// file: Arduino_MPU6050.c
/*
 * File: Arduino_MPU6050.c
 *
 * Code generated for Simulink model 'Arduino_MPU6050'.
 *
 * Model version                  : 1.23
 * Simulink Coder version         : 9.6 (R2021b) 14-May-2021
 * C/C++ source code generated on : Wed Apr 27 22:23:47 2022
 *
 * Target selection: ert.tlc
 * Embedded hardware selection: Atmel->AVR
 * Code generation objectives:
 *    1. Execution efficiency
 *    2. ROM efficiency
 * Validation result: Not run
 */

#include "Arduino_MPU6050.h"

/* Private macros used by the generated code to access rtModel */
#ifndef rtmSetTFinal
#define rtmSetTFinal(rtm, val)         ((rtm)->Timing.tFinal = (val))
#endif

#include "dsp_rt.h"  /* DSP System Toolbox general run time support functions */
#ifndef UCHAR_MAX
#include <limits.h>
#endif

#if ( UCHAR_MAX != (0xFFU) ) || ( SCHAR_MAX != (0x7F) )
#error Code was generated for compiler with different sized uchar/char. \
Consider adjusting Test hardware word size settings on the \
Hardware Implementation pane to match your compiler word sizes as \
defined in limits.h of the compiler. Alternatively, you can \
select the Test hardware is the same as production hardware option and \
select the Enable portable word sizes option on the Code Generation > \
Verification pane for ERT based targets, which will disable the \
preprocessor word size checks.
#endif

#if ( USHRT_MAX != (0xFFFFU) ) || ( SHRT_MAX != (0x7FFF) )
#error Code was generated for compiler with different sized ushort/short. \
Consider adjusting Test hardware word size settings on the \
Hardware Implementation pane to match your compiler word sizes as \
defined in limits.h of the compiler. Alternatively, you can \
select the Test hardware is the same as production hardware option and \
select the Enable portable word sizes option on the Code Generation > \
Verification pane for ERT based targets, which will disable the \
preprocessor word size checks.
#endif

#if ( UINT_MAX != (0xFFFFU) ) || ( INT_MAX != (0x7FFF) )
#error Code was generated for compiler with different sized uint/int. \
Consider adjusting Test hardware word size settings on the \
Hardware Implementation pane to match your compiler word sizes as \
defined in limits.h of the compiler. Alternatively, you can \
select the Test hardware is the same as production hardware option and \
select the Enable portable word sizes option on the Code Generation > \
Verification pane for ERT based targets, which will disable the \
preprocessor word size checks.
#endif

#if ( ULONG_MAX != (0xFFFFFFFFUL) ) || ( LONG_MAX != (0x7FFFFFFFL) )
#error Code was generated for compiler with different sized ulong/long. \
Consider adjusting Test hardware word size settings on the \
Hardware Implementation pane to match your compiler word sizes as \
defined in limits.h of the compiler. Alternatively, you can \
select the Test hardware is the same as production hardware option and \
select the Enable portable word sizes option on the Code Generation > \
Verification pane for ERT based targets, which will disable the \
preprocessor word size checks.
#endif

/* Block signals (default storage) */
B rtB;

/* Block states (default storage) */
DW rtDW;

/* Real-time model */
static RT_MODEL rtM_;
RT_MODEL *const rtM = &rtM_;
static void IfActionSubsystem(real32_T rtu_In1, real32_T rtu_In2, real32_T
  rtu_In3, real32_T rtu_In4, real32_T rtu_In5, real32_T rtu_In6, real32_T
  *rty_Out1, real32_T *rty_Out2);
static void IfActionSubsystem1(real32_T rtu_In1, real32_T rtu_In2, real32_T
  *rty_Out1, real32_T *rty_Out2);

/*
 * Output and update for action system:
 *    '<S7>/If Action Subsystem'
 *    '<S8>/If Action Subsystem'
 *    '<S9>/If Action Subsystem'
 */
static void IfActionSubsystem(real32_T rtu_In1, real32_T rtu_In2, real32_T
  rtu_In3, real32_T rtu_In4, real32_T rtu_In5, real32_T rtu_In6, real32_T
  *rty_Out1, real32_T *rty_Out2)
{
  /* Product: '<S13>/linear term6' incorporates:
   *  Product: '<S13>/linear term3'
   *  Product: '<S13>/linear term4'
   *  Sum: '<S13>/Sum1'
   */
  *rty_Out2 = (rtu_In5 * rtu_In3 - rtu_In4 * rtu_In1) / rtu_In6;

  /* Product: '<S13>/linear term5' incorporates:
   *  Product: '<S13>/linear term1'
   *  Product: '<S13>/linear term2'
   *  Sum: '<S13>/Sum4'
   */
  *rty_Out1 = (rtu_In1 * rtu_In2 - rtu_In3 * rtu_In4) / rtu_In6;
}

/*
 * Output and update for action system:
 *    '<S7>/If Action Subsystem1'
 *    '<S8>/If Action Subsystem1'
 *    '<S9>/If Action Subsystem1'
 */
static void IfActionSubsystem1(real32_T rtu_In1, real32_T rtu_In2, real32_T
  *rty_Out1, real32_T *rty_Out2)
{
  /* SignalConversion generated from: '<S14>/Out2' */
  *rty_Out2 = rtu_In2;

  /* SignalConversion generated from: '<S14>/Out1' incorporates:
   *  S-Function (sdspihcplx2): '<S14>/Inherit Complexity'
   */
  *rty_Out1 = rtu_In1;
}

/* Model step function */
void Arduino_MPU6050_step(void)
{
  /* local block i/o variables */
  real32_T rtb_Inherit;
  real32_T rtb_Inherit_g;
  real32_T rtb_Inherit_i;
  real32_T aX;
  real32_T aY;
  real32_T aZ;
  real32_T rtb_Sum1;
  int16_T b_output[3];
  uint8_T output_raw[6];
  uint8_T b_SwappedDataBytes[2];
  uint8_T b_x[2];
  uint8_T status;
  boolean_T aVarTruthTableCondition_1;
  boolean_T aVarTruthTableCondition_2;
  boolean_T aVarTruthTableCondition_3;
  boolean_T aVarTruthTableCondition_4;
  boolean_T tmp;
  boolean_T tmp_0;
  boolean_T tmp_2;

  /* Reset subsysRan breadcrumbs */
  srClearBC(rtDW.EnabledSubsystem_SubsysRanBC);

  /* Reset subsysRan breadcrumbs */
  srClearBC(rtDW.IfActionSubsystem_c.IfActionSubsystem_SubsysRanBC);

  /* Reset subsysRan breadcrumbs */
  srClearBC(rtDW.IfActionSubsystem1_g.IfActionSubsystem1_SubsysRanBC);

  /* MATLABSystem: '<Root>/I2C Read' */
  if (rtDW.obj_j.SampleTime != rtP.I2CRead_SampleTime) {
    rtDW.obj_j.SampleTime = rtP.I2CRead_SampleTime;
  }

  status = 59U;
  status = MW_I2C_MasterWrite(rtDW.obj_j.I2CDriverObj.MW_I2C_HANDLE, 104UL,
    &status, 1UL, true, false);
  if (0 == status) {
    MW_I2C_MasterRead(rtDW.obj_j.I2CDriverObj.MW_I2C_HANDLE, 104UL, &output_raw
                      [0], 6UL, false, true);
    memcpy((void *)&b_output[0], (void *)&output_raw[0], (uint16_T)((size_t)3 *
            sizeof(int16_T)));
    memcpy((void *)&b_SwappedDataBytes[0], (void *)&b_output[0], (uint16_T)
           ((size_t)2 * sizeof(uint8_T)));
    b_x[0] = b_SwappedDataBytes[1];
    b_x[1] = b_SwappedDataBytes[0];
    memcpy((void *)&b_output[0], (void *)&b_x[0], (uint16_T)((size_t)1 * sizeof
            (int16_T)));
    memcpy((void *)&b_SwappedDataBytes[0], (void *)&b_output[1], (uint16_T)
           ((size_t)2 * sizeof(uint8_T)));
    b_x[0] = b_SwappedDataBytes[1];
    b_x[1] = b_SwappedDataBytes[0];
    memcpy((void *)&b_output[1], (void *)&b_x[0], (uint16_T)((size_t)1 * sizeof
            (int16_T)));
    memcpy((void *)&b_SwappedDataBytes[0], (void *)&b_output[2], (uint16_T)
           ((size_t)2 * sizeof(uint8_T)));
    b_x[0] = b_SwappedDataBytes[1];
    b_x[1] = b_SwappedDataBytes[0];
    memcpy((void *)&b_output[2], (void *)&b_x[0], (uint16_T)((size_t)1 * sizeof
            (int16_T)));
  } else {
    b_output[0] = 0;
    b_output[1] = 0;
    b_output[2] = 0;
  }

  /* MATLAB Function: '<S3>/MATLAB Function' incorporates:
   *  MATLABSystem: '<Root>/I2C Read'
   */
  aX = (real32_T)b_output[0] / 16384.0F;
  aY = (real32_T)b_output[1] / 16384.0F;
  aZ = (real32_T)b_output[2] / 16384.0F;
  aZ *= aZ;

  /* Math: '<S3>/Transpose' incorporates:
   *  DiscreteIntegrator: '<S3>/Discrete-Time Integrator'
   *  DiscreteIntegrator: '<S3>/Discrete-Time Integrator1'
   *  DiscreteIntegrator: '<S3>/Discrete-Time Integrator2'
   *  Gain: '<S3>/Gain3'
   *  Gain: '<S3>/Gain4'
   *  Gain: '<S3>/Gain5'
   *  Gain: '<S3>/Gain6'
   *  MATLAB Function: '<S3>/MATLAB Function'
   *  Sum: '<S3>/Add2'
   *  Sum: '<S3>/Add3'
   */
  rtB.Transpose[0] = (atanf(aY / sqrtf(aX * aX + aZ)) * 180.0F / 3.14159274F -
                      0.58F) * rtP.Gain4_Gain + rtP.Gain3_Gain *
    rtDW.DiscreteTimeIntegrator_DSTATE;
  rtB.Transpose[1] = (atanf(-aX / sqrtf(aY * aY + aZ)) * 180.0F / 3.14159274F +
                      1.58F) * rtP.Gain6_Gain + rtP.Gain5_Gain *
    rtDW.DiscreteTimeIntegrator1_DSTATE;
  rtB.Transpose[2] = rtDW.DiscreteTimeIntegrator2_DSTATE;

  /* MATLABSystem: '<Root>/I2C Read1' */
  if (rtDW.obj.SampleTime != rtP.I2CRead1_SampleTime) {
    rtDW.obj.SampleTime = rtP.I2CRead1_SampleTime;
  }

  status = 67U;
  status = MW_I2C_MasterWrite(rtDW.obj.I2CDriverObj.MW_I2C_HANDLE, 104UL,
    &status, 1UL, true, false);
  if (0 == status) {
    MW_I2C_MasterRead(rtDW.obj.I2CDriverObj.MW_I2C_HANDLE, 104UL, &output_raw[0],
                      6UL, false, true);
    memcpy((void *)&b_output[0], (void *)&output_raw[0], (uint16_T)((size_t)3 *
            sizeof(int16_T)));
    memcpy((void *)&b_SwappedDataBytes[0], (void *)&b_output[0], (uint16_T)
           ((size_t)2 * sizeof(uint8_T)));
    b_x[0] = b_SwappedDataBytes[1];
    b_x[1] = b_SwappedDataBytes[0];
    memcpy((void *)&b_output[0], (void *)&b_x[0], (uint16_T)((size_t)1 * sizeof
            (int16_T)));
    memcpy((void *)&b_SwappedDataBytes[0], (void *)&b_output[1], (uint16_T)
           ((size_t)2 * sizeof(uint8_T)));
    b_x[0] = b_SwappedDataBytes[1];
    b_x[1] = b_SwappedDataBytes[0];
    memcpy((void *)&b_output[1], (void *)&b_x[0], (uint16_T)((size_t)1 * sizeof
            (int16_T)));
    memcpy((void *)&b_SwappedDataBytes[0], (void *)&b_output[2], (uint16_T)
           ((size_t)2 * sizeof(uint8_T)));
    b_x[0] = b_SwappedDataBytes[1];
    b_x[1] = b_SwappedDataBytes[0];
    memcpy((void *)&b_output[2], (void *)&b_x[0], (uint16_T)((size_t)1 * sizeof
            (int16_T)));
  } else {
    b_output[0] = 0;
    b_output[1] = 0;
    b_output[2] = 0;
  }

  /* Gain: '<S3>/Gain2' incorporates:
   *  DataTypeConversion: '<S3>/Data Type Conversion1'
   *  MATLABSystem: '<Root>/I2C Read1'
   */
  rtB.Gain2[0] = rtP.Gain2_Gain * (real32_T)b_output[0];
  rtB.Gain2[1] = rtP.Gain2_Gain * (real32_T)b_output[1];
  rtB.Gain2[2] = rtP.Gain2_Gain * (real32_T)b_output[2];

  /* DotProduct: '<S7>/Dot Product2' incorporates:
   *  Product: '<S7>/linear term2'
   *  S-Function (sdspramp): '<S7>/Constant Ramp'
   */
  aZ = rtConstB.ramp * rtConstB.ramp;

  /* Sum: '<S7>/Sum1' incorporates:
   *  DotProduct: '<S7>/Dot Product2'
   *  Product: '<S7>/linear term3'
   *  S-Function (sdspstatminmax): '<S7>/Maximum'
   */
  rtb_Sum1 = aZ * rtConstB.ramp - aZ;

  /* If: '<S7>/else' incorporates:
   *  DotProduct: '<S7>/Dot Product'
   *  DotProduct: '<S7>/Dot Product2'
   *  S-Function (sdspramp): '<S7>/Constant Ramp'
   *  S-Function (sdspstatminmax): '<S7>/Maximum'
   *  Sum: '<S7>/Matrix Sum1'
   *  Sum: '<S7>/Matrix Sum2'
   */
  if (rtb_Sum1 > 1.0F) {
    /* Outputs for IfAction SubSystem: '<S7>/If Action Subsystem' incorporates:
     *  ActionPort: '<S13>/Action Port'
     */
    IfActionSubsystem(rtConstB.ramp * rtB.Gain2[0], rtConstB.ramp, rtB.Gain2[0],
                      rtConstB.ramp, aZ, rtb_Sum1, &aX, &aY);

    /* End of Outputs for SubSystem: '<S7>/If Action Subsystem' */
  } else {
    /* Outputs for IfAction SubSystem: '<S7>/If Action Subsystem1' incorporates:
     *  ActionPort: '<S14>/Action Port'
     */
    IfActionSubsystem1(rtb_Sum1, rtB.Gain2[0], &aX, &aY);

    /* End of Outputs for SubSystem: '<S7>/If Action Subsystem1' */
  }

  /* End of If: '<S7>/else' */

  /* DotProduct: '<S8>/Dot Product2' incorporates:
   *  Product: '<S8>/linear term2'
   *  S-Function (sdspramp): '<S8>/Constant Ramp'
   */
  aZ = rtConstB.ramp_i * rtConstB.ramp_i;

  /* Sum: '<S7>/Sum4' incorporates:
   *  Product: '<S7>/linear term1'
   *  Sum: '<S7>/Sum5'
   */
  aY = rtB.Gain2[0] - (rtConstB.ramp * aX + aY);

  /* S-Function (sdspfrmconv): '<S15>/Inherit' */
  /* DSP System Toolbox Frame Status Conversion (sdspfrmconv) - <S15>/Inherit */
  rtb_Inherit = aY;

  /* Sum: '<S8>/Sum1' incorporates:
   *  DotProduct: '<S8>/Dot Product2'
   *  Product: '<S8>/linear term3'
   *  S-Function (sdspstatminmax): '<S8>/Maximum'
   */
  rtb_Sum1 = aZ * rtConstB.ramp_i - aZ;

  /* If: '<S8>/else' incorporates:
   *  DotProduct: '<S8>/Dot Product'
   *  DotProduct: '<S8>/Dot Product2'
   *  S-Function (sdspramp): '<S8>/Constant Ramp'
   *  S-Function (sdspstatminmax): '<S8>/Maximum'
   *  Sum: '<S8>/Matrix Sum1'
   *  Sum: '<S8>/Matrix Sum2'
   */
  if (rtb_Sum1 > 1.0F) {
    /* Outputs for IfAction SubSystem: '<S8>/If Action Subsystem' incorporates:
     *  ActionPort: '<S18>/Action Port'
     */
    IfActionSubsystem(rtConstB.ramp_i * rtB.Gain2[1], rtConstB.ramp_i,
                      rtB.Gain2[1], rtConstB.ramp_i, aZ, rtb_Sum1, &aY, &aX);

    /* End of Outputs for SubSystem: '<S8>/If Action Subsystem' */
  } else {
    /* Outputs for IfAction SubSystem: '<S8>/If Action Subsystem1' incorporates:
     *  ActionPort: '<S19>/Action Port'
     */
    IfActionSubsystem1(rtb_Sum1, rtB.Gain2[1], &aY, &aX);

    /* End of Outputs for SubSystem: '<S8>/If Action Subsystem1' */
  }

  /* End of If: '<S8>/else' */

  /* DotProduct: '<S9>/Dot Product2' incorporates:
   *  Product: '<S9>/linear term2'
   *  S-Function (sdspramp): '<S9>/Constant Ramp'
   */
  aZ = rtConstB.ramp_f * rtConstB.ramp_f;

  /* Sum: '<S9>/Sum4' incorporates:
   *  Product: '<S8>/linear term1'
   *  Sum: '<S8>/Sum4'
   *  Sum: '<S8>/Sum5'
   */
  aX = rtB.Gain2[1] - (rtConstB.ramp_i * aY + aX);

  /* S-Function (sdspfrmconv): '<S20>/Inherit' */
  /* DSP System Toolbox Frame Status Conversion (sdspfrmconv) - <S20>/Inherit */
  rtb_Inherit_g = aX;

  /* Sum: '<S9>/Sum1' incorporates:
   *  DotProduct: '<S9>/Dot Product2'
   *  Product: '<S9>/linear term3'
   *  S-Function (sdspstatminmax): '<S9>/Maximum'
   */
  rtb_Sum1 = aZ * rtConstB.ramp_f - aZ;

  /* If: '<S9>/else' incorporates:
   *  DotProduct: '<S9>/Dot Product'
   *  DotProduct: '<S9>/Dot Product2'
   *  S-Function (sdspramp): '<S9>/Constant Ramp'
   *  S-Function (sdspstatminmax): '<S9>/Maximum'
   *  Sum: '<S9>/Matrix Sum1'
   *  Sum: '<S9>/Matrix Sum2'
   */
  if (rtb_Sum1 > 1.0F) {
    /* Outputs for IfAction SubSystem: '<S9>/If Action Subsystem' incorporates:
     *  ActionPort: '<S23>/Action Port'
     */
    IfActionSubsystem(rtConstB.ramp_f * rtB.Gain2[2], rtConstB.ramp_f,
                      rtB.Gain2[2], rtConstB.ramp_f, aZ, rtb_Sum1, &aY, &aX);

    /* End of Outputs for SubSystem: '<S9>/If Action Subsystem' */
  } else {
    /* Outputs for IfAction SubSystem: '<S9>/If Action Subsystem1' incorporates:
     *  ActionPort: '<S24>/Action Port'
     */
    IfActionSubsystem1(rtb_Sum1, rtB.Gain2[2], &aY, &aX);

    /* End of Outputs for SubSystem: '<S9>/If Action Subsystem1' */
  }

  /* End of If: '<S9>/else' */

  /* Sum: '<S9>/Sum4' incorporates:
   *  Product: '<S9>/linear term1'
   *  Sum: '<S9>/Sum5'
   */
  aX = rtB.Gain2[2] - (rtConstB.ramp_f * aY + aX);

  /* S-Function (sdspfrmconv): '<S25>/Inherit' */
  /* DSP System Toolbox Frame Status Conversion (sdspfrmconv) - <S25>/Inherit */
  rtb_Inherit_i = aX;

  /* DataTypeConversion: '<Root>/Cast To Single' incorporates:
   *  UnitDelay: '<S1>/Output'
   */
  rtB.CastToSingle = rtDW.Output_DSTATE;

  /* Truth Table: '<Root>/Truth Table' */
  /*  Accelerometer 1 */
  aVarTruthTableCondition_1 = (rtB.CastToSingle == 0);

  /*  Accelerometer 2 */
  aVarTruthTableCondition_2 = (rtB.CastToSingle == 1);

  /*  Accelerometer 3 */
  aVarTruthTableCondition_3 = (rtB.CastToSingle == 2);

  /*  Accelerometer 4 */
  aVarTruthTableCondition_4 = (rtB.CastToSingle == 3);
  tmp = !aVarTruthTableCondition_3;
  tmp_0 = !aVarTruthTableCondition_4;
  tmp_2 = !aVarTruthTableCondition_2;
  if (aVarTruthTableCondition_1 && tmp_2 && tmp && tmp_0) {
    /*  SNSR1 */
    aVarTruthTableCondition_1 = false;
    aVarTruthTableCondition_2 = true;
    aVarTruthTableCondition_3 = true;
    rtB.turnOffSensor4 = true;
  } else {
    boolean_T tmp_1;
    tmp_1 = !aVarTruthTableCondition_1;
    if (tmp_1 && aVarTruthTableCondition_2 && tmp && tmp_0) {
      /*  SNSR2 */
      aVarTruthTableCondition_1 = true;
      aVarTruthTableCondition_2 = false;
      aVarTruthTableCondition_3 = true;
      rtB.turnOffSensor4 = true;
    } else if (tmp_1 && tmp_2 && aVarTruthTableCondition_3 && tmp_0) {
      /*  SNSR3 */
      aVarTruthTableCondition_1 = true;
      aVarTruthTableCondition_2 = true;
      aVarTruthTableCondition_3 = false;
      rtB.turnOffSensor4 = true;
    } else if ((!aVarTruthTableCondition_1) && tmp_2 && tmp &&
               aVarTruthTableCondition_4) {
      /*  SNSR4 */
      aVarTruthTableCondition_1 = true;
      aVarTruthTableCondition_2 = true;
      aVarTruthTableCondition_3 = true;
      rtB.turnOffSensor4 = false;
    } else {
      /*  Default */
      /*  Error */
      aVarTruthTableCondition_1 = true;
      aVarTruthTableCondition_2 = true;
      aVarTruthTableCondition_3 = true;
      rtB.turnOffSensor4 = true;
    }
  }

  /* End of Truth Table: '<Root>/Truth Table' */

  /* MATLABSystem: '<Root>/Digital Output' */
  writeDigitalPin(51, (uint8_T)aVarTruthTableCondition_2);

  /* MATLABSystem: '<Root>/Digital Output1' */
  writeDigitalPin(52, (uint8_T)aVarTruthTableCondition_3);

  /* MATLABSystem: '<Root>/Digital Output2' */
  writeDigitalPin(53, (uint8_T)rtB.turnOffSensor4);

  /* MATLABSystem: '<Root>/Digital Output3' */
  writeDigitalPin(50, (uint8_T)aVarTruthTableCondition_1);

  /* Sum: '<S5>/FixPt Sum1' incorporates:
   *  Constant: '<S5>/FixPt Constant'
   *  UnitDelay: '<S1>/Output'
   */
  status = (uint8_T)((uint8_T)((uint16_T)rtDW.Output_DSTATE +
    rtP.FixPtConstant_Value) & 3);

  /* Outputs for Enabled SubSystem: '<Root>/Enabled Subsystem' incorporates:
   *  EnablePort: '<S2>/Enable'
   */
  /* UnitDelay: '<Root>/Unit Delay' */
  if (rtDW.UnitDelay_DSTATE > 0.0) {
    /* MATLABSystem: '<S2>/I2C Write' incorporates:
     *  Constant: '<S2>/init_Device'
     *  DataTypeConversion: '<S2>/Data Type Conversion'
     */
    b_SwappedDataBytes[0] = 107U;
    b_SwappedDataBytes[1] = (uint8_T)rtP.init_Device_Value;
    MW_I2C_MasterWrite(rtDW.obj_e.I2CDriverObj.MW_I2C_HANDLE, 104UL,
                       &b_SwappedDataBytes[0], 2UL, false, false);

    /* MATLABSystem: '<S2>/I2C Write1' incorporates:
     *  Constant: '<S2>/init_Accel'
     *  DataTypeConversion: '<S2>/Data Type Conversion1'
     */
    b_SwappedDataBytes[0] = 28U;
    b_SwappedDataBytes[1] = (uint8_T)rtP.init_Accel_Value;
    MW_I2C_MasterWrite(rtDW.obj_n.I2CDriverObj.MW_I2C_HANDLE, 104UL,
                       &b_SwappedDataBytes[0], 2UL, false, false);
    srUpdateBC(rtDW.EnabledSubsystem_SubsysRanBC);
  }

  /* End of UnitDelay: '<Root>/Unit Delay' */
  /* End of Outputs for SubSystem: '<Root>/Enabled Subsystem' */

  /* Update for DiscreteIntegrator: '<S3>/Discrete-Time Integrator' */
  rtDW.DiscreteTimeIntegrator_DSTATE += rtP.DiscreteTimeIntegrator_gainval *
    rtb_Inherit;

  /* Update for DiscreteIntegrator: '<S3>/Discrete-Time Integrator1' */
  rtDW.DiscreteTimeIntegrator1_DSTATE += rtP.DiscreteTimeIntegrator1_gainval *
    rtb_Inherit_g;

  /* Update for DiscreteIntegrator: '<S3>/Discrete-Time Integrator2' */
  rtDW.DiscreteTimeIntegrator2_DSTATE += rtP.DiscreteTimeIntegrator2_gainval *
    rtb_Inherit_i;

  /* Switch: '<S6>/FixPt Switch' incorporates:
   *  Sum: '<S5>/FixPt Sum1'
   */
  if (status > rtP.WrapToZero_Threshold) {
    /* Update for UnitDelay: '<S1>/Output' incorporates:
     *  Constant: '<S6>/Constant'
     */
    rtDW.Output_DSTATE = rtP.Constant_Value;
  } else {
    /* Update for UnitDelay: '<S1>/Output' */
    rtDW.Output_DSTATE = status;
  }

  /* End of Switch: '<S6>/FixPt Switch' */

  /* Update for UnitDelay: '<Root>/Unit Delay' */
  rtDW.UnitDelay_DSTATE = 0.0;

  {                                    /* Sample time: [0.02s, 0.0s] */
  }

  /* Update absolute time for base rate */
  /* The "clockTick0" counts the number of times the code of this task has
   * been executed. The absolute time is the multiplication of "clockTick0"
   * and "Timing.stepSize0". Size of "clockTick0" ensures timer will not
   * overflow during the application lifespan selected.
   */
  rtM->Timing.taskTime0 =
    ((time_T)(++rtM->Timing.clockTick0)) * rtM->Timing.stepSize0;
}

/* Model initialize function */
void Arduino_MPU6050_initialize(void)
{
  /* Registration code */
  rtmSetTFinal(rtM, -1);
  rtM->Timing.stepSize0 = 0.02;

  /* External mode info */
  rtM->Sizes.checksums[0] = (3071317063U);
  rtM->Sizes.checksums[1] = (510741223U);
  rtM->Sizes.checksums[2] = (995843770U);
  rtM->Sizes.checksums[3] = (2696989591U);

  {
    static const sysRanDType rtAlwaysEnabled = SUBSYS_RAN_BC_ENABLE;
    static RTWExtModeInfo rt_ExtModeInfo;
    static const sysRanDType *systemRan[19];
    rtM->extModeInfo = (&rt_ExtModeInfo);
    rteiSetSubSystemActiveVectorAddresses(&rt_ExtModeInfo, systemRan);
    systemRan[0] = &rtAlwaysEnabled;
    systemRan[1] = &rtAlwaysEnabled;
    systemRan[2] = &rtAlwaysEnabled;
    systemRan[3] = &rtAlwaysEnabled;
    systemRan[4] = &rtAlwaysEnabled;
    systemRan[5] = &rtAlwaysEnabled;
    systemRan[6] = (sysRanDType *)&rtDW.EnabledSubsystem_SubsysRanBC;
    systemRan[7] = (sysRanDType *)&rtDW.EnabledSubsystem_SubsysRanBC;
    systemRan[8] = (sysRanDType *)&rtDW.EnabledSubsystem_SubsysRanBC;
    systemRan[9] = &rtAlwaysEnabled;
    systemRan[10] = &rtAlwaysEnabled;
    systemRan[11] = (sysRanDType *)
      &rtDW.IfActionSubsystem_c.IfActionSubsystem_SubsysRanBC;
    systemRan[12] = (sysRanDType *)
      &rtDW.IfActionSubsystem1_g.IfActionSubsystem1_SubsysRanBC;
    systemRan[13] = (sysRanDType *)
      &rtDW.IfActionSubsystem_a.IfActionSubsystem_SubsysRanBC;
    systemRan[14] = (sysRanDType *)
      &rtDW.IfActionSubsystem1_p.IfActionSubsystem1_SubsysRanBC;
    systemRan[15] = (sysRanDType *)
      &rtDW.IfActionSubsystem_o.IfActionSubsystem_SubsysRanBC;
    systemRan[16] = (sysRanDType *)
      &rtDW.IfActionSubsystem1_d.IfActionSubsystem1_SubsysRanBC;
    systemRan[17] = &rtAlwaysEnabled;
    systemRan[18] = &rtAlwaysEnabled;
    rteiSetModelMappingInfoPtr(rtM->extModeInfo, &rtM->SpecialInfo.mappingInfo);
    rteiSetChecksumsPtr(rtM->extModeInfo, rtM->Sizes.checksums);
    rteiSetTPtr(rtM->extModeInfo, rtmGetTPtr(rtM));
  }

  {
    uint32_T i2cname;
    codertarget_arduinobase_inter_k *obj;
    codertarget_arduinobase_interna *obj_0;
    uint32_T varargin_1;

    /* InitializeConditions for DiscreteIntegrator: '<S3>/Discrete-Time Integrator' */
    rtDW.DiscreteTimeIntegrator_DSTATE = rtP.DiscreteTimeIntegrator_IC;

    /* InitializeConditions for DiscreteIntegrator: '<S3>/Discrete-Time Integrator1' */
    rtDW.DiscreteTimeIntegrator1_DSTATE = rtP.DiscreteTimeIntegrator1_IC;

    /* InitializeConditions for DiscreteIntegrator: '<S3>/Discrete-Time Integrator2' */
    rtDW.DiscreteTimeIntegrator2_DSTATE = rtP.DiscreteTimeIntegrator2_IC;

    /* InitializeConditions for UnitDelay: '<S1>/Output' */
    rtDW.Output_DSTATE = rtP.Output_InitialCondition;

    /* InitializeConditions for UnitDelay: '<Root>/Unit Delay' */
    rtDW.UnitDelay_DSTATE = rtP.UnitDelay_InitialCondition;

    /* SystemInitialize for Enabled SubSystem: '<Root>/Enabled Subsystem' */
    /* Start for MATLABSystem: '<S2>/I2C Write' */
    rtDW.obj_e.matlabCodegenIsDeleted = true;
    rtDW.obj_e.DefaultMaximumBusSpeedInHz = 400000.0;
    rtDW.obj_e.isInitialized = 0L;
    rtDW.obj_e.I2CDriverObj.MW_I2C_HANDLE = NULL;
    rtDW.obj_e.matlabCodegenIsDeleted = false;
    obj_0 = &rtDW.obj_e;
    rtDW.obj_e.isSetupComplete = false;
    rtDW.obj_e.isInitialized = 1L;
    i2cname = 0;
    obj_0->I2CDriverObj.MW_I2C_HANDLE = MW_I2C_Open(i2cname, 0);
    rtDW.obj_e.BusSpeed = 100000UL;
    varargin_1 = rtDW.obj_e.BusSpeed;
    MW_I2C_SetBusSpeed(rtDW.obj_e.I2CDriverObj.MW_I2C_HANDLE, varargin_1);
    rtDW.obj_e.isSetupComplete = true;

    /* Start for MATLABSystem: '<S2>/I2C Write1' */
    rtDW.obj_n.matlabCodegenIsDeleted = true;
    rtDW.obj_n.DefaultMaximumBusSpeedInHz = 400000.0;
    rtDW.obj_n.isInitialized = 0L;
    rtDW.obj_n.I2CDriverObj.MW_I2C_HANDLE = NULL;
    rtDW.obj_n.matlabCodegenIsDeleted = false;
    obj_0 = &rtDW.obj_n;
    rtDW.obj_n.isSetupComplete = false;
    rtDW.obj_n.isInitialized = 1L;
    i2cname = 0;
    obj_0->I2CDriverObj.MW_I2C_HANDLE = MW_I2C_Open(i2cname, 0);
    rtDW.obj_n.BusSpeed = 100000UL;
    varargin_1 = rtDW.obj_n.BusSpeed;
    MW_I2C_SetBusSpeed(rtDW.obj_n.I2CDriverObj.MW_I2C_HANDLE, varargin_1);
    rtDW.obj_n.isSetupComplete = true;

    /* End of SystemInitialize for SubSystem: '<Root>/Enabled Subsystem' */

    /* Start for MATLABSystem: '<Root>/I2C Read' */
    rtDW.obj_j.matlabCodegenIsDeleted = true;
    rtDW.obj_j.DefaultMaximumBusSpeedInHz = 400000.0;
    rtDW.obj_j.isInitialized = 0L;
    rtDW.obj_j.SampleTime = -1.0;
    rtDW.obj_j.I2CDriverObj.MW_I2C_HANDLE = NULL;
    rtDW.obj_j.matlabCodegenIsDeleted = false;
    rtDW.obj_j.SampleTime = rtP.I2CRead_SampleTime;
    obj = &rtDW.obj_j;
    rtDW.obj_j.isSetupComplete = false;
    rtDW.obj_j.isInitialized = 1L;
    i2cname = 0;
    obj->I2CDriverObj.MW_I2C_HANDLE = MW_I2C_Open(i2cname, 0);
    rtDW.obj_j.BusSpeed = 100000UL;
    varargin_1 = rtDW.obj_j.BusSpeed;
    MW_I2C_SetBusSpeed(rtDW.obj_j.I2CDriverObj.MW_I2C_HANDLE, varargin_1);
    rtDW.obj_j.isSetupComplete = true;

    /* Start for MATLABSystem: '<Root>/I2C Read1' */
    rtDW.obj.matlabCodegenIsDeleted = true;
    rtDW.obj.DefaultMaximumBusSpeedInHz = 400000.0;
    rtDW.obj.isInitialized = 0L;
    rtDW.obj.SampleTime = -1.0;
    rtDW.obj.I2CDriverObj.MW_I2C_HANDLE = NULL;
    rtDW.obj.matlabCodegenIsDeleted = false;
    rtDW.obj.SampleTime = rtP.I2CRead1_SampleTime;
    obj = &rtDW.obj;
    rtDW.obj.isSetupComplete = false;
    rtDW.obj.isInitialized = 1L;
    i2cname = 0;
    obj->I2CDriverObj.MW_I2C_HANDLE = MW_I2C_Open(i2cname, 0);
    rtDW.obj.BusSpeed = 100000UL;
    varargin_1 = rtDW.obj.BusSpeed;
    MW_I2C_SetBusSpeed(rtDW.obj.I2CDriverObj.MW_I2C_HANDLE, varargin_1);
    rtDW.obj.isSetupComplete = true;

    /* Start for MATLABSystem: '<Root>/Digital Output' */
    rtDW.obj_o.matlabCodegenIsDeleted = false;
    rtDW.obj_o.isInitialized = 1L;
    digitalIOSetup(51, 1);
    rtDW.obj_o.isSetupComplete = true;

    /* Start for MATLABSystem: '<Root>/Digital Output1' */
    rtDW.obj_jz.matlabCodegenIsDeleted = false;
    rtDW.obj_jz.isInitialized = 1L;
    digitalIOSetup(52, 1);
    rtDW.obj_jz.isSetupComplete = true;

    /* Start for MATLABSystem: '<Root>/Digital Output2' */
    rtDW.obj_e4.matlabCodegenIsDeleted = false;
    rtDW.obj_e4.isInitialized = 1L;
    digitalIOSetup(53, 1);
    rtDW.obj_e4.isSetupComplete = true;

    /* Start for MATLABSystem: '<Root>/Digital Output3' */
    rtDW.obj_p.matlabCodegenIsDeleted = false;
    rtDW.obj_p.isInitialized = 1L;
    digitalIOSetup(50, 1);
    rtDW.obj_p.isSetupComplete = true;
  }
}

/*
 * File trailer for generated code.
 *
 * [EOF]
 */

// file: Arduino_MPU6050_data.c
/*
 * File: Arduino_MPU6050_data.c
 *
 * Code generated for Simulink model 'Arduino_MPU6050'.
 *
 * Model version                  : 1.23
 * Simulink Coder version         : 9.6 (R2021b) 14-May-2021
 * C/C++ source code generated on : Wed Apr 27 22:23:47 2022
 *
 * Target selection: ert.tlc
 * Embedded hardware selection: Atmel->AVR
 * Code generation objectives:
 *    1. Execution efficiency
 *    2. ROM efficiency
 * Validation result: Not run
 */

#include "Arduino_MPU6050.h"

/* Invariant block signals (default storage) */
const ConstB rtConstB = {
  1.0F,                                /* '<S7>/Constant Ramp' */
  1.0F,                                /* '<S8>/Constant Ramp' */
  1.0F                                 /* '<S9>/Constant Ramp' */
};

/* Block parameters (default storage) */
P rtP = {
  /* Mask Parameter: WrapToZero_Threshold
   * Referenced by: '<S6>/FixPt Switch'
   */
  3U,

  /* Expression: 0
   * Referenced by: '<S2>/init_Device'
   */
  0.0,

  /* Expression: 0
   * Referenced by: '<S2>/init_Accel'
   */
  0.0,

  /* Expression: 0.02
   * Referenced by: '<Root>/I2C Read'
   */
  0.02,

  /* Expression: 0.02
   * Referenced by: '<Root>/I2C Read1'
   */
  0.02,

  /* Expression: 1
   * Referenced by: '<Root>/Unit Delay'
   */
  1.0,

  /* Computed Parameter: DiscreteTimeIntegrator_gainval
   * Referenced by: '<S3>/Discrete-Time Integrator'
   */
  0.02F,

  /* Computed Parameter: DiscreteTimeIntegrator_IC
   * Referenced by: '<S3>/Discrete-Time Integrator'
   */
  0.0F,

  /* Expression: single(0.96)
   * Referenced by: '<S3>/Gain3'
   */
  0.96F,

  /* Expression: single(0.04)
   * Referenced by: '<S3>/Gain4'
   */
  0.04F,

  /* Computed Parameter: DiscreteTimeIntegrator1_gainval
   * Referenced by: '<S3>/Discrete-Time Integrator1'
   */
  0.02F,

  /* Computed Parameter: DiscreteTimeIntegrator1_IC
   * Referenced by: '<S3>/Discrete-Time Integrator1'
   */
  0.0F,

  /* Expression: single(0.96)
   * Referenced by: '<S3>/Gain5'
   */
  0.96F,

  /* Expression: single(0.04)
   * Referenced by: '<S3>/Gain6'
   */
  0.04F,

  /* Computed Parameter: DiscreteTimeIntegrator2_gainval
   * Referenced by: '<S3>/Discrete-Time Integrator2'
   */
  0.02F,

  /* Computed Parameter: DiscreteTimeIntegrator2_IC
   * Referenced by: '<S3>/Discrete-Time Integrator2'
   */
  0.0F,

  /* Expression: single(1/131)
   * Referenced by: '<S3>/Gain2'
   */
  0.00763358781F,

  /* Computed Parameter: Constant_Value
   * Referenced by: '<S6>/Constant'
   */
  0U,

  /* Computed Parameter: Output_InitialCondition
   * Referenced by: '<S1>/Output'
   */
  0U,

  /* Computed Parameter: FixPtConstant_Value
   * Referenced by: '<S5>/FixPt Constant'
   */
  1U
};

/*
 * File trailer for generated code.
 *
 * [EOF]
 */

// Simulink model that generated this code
simulink model "Arduino_MPU6050"  (R2021b)
settings: Solver=FixedStepDiscrete  StartTime=0.0  StopTime=inf  RelTol=1e-3  EnableMultiTasking=on
PostLoadFcn:
  | Simulink.importExternalCTypes('wire.h', 'EnumClass', 'dynamic');
undefined symbols (not defined in the file): DiscIntNeverNeededParam
libraries: arduinolib x10, simulink x1

== system Arduino_MPU6050 ==
  Cast To Single : DataTypeConversion  OutDataTypeStr=uint8
  Counter Free-Running : simulink/Sources/Counter Free-Running  NumBits=2  tsamp=0.02
  Digital Output : arduinolib/Digital Output  pinNumber=51  Direction=output  blockPlatform=arduino
  Digital Output1 : arduinolib/Digital Output  pinNumber=52  Direction=output  blockPlatform=arduino
  Digital Output2 : arduinolib/Digital Output  pinNumber=53  Direction=output  blockPlatform=arduino
  Digital Output3 : arduinolib/Digital Output  pinNumber=50  Direction=output  blockPlatform=arduino
  Enabled Subsystem : Subsystem  TreatAsAtomicUnit=on
  Ground : Ground
  I2C Read : arduinolib/I2C Read  I2CModule=0  Mode=Master  SlaveAddress=uint8(hex2dec('68'))  SlaveByteOrder=BigEndian  Direction=Receiver  RegisterAddressMode=on  RegisterAddress=uint8(hex2dec('3B'))  SlaveDataType=int16  DataLength=3  NoAck=off  RepeatedStart=off  OutputStatus=off  blockPlatform=ARDUINO  SampleTime=0.02
  I2C Read1 : arduinolib/I2C Read  I2CModule=0  Mode=Master  SlaveAddress=uint8(hex2dec('68'))  SlaveByteOrder=BigEndian  Direction=Receiver  RegisterAddressMode=on  RegisterAddress=uint8(hex2dec('43'))  SlaveDataType=int16  DataLength=3  NoAck=off  RepeatedStart=off  OutputStatus=off  blockPlatform=ARDUINO  SampleTime=0.02
  Scope : Scope
  Scope1 : Scope
  Scope2 : Scope
  Serial Receive : arduinolib/Serial Receive  Commented=on  isARMArch=off  portNumber=1  DataType=single  Datalength=3  SampleTime=0.02  showOutStatus=on  blockPlatform=arduino
  Serial Transmit : arduinolib/Serial Transmit  Commented=on  portNumber=1  sendmode=print  label=;  sendformat=Decimal  floatprecision=3  blockPlatform=arduino
  Subsystem : Subsystem
  Truth Table : Truth Table  TreatAsAtomicUnit=on
  Unit Delay : UnitDelay  InitialCondition=1  SampleTime=-1  HasFrameUpgradeWarning=on
  wires:
  Ground/1 -> Unit Delay/1
  Unit Delay/1 -> Enabled Subsystem/Enable
  I2C Read/1 -> Subsystem/1(In1)
  I2C Read1/1 -> Subsystem/2(In2)
  Cast To Single/1 -> Scope2/1, Truth Table/1(turnOn)
  Counter Free-Running/1 -> Cast To Single/1
  Subsystem/1(Out1) -> Scope1/1, Serial Transmit/1
  Truth Table/1(turnOffSensor1) -> Digital Output3/1
  Truth Table/2(turnOffSensor2) -> Digital Output/1
  Truth Table/3(turnOffSensor3) -> Digital Output1/1
  Truth Table/4(turnOffSensor4) -> Scope/1, Digital Output2/1

== system Arduino_MPU6050/Enabled Subsystem ==
  Enable : EnablePort
  C Caller : CCaller  FunctionName=setup
  C Function : CFunction
  Data Type Conversion : DataTypeConversion  OutDataTypeStr=uint8  RndMeth=Simplest
  Data Type Conversion1 : DataTypeConversion  OutDataTypeStr=uint8  RndMeth=Simplest
  I2C Write : arduinolib/I2C Write  I2CModule=0  Mode=Master  SlaveAddress=uint8(hex2dec('68'))  SlaveByteOrder=BigEndian  Direction=Transmitter  RegisterAddressMode=on  RegisterAddress=uint8(hex2dec('6B'))  SlaveDataType=uint8  DataLength=1  NoAck=off  RepeatedStart=off  OutputStatus=off  blockPlatform=ARDUINO
  I2C Write1 : arduinolib/I2C Write  I2CModule=0  Mode=Master  SlaveAddress=uint8(hex2dec('68'))  SlaveByteOrder=BigEndian  Direction=Transmitter  RegisterAddressMode=on  RegisterAddress=uint8(hex2dec('1C'))  SlaveDataType=uint8  DataLength=1  NoAck=off  RepeatedStart=off  OutputStatus=off  blockPlatform=ARDUINO
  Subsystem : Subsystem  mask{filename=wire.h}
  init_Accel : Constant  Value=0
  init_Device : Constant  Value=0
  wires:
  init_Device/1 -> Data Type Conversion/1
  init_Accel/1 -> Data Type Conversion1/1
  Data Type Conversion/1 -> I2C Write/1
  Data Type Conversion1/1 -> I2C Write1/1

== system Arduino_MPU6050/Subsystem ==
  In1 : Inport
  In2 : Inport  Port=2
  Add2 : Sum
  Add3 : Sum
  Data Type Conversion : DataTypeConversion  OutDataTypeStr=single
  Data Type Conversion1 : DataTypeConversion  OutDataTypeStr=single
  Demux1 : Demux  Outputs=3
  Discrete-Time Integrator : DiscreteIntegrator  SampleTime=-1  ICPrevOutput=DiscIntNeverNeededParam  ICPrevScaledInput=DiscIntNeverNeededParam
  Discrete-Time Integrator1 : DiscreteIntegrator  SampleTime=-1  ICPrevOutput=DiscIntNeverNeededParam  ICPrevScaledInput=DiscIntNeverNeededParam
  Discrete-Time Integrator2 : DiscreteIntegrator  SampleTime=-1  ICPrevOutput=DiscIntNeverNeededParam  ICPrevScaledInput=DiscIntNeverNeededParam
  Gain2 : Gain  Gain=single(1/131)
  Gain3 : Gain  Gain=single(0.96)
  Gain4 : Gain  Gain=single(0.04)
  Gain5 : Gain  Gain=single(0.96)  ParamDataTypeStr=single
  Gain6 : Gain  Gain=single(0.04)  ParamDataTypeStr=single
  MATLAB Function : MATLAB Function  TreatAsAtomicUnit=on
  Mux1 : Mux  Inputs=3
  Transpose : Math  Operator=transpose  SaturateOnIntegerOverflow=on
  Out1 : Outport
  wires:
  MATLAB Function/2(aAngY) -> Gain6/1  "aAngY"
  Mux1/1 -> Transpose/1
  Add3/1 -> Mux1/2  "pitch"
  Demux1/1 -> Discrete-Time Integrator/1
  Gain3/1 -> Add2/1
  Gain4/1 -> Add2/2
  Add2/1 -> Mux1/1  "roll"
  Discrete-Time Integrator2/1 -> Mux1/3  "yaw"
  Discrete-Time Integrator/1 -> Gain3/1
  Discrete-Time Integrator1/1 -> Gain5/1
  Gain6/1 -> Add3/2
  Gain5/1 -> Add3/1
  Demux1/3 -> Discrete-Time Integrator2/1
  Demux1/2 -> Discrete-Time Integrator1/1
  Gain2/1 -> Demux1/1
  Data Type Conversion1/1 -> Gain2/1
  In2/1 -> Data Type Conversion1/1
  In1/1 -> Data Type Conversion/1
  Data Type Conversion/1 -> MATLAB Function/1(u)
  MATLAB Function/1(aAngX) -> Gain4/1  "aAngX"
  Transpose/1 -> Out1/1

== system Arduino_MPU6050/Enabled Subsystem/Subsystem ==

== matlab function Arduino_MPU6050/Truth Table ==
function [turnOffSensor1,turnOffSensor2, turnOffSensor3, turnOffSensor4] = fcn(turnOn)

aVarTruthTableCondition_1 = false;
aVarTruthTableCondition_2 = false;
aVarTruthTableCondition_3 = false;
aVarTruthTableCondition_4 = false;

% Accelerometer 1

aVarTruthTableCondition_1 = logical(turnOn==uint8(0));

% Accelerometer 2

aVarTruthTableCondition_2 = logical(turnOn==uint8(1));

% Accelerometer 3

aVarTruthTableCondition_3 = logical(turnOn==uint8(2));

% Accelerometer 4

aVarTruthTableCondition_4 = logical(turnOn==uint8(3));

if (aVarTruthTableCondition_1 && ~aVarTruthTableCondition_2 && ~aVarTruthTableCondition_3 && ~aVarTruthTableCondition_4)
    Sensor1On();
elseif (~aVarTruthTableCondition_1 && aVarTruthTableCondition_2 && ~aVarTruthTableCondition_3 && ~aVarTruthTableCondition_4)
    Sensor2On();
elseif (~aVarTruthTableCondition_1 && ~aVarTruthTableCondition_2 && aVarTruthTableCondition_3 && ~aVarTruthTableCondition_4)
    Sensor3On();
elseif (~aVarTruthTableCondition_1 && ~aVarTruthTableCondition_2 && ~aVarTruthTableCondition_3 && aVarTruthTableCondition_4)
    Sensor4On();
else % Default
    SensorError();
end

function Sensor1On()

% SNSR1

turnOffSensor1 = false;
turnOffSensor2 = true;
turnOffSensor3 = true;
turnOffSensor4 = true;

function Sensor2On()

% SNSR2

turnOffSensor1 = true;
turnOffSensor2 = false;
turnOffSensor3 = true;
turnOffSensor4 = true;

function Sensor3On()

% SNSR3

turnOffSensor1 = true;
turnOffSensor2 = true;
turnOffSensor3 = false;
turnOffSensor4 = true;

function Sensor4On()

% SNSR4

turnOffSensor1 = true;
turnOffSensor2 = true;
turnOffSensor3 = true;
turnOffSensor4 = false;

function SensorError()

% Error

turnOffSensor1 = true;
turnOffSensor2 = true;
turnOffSensor3 = true;
turnOffSensor4 = true;

== matlab function Arduino_MPU6050/Subsystem/MATLAB Function ==
function [aAngX,aAngY] = fcn(u)
aX=u(1)/16384; aY=u(2)/16384; aZ=u(3)/16384;
aAngX = atan(aY / sqrt(aX^2+aZ^2))*180/pi - 0.58;
aAngY = atan(-aX/ sqrt(aY^2+aZ^2))*180/pi + 1.58;
